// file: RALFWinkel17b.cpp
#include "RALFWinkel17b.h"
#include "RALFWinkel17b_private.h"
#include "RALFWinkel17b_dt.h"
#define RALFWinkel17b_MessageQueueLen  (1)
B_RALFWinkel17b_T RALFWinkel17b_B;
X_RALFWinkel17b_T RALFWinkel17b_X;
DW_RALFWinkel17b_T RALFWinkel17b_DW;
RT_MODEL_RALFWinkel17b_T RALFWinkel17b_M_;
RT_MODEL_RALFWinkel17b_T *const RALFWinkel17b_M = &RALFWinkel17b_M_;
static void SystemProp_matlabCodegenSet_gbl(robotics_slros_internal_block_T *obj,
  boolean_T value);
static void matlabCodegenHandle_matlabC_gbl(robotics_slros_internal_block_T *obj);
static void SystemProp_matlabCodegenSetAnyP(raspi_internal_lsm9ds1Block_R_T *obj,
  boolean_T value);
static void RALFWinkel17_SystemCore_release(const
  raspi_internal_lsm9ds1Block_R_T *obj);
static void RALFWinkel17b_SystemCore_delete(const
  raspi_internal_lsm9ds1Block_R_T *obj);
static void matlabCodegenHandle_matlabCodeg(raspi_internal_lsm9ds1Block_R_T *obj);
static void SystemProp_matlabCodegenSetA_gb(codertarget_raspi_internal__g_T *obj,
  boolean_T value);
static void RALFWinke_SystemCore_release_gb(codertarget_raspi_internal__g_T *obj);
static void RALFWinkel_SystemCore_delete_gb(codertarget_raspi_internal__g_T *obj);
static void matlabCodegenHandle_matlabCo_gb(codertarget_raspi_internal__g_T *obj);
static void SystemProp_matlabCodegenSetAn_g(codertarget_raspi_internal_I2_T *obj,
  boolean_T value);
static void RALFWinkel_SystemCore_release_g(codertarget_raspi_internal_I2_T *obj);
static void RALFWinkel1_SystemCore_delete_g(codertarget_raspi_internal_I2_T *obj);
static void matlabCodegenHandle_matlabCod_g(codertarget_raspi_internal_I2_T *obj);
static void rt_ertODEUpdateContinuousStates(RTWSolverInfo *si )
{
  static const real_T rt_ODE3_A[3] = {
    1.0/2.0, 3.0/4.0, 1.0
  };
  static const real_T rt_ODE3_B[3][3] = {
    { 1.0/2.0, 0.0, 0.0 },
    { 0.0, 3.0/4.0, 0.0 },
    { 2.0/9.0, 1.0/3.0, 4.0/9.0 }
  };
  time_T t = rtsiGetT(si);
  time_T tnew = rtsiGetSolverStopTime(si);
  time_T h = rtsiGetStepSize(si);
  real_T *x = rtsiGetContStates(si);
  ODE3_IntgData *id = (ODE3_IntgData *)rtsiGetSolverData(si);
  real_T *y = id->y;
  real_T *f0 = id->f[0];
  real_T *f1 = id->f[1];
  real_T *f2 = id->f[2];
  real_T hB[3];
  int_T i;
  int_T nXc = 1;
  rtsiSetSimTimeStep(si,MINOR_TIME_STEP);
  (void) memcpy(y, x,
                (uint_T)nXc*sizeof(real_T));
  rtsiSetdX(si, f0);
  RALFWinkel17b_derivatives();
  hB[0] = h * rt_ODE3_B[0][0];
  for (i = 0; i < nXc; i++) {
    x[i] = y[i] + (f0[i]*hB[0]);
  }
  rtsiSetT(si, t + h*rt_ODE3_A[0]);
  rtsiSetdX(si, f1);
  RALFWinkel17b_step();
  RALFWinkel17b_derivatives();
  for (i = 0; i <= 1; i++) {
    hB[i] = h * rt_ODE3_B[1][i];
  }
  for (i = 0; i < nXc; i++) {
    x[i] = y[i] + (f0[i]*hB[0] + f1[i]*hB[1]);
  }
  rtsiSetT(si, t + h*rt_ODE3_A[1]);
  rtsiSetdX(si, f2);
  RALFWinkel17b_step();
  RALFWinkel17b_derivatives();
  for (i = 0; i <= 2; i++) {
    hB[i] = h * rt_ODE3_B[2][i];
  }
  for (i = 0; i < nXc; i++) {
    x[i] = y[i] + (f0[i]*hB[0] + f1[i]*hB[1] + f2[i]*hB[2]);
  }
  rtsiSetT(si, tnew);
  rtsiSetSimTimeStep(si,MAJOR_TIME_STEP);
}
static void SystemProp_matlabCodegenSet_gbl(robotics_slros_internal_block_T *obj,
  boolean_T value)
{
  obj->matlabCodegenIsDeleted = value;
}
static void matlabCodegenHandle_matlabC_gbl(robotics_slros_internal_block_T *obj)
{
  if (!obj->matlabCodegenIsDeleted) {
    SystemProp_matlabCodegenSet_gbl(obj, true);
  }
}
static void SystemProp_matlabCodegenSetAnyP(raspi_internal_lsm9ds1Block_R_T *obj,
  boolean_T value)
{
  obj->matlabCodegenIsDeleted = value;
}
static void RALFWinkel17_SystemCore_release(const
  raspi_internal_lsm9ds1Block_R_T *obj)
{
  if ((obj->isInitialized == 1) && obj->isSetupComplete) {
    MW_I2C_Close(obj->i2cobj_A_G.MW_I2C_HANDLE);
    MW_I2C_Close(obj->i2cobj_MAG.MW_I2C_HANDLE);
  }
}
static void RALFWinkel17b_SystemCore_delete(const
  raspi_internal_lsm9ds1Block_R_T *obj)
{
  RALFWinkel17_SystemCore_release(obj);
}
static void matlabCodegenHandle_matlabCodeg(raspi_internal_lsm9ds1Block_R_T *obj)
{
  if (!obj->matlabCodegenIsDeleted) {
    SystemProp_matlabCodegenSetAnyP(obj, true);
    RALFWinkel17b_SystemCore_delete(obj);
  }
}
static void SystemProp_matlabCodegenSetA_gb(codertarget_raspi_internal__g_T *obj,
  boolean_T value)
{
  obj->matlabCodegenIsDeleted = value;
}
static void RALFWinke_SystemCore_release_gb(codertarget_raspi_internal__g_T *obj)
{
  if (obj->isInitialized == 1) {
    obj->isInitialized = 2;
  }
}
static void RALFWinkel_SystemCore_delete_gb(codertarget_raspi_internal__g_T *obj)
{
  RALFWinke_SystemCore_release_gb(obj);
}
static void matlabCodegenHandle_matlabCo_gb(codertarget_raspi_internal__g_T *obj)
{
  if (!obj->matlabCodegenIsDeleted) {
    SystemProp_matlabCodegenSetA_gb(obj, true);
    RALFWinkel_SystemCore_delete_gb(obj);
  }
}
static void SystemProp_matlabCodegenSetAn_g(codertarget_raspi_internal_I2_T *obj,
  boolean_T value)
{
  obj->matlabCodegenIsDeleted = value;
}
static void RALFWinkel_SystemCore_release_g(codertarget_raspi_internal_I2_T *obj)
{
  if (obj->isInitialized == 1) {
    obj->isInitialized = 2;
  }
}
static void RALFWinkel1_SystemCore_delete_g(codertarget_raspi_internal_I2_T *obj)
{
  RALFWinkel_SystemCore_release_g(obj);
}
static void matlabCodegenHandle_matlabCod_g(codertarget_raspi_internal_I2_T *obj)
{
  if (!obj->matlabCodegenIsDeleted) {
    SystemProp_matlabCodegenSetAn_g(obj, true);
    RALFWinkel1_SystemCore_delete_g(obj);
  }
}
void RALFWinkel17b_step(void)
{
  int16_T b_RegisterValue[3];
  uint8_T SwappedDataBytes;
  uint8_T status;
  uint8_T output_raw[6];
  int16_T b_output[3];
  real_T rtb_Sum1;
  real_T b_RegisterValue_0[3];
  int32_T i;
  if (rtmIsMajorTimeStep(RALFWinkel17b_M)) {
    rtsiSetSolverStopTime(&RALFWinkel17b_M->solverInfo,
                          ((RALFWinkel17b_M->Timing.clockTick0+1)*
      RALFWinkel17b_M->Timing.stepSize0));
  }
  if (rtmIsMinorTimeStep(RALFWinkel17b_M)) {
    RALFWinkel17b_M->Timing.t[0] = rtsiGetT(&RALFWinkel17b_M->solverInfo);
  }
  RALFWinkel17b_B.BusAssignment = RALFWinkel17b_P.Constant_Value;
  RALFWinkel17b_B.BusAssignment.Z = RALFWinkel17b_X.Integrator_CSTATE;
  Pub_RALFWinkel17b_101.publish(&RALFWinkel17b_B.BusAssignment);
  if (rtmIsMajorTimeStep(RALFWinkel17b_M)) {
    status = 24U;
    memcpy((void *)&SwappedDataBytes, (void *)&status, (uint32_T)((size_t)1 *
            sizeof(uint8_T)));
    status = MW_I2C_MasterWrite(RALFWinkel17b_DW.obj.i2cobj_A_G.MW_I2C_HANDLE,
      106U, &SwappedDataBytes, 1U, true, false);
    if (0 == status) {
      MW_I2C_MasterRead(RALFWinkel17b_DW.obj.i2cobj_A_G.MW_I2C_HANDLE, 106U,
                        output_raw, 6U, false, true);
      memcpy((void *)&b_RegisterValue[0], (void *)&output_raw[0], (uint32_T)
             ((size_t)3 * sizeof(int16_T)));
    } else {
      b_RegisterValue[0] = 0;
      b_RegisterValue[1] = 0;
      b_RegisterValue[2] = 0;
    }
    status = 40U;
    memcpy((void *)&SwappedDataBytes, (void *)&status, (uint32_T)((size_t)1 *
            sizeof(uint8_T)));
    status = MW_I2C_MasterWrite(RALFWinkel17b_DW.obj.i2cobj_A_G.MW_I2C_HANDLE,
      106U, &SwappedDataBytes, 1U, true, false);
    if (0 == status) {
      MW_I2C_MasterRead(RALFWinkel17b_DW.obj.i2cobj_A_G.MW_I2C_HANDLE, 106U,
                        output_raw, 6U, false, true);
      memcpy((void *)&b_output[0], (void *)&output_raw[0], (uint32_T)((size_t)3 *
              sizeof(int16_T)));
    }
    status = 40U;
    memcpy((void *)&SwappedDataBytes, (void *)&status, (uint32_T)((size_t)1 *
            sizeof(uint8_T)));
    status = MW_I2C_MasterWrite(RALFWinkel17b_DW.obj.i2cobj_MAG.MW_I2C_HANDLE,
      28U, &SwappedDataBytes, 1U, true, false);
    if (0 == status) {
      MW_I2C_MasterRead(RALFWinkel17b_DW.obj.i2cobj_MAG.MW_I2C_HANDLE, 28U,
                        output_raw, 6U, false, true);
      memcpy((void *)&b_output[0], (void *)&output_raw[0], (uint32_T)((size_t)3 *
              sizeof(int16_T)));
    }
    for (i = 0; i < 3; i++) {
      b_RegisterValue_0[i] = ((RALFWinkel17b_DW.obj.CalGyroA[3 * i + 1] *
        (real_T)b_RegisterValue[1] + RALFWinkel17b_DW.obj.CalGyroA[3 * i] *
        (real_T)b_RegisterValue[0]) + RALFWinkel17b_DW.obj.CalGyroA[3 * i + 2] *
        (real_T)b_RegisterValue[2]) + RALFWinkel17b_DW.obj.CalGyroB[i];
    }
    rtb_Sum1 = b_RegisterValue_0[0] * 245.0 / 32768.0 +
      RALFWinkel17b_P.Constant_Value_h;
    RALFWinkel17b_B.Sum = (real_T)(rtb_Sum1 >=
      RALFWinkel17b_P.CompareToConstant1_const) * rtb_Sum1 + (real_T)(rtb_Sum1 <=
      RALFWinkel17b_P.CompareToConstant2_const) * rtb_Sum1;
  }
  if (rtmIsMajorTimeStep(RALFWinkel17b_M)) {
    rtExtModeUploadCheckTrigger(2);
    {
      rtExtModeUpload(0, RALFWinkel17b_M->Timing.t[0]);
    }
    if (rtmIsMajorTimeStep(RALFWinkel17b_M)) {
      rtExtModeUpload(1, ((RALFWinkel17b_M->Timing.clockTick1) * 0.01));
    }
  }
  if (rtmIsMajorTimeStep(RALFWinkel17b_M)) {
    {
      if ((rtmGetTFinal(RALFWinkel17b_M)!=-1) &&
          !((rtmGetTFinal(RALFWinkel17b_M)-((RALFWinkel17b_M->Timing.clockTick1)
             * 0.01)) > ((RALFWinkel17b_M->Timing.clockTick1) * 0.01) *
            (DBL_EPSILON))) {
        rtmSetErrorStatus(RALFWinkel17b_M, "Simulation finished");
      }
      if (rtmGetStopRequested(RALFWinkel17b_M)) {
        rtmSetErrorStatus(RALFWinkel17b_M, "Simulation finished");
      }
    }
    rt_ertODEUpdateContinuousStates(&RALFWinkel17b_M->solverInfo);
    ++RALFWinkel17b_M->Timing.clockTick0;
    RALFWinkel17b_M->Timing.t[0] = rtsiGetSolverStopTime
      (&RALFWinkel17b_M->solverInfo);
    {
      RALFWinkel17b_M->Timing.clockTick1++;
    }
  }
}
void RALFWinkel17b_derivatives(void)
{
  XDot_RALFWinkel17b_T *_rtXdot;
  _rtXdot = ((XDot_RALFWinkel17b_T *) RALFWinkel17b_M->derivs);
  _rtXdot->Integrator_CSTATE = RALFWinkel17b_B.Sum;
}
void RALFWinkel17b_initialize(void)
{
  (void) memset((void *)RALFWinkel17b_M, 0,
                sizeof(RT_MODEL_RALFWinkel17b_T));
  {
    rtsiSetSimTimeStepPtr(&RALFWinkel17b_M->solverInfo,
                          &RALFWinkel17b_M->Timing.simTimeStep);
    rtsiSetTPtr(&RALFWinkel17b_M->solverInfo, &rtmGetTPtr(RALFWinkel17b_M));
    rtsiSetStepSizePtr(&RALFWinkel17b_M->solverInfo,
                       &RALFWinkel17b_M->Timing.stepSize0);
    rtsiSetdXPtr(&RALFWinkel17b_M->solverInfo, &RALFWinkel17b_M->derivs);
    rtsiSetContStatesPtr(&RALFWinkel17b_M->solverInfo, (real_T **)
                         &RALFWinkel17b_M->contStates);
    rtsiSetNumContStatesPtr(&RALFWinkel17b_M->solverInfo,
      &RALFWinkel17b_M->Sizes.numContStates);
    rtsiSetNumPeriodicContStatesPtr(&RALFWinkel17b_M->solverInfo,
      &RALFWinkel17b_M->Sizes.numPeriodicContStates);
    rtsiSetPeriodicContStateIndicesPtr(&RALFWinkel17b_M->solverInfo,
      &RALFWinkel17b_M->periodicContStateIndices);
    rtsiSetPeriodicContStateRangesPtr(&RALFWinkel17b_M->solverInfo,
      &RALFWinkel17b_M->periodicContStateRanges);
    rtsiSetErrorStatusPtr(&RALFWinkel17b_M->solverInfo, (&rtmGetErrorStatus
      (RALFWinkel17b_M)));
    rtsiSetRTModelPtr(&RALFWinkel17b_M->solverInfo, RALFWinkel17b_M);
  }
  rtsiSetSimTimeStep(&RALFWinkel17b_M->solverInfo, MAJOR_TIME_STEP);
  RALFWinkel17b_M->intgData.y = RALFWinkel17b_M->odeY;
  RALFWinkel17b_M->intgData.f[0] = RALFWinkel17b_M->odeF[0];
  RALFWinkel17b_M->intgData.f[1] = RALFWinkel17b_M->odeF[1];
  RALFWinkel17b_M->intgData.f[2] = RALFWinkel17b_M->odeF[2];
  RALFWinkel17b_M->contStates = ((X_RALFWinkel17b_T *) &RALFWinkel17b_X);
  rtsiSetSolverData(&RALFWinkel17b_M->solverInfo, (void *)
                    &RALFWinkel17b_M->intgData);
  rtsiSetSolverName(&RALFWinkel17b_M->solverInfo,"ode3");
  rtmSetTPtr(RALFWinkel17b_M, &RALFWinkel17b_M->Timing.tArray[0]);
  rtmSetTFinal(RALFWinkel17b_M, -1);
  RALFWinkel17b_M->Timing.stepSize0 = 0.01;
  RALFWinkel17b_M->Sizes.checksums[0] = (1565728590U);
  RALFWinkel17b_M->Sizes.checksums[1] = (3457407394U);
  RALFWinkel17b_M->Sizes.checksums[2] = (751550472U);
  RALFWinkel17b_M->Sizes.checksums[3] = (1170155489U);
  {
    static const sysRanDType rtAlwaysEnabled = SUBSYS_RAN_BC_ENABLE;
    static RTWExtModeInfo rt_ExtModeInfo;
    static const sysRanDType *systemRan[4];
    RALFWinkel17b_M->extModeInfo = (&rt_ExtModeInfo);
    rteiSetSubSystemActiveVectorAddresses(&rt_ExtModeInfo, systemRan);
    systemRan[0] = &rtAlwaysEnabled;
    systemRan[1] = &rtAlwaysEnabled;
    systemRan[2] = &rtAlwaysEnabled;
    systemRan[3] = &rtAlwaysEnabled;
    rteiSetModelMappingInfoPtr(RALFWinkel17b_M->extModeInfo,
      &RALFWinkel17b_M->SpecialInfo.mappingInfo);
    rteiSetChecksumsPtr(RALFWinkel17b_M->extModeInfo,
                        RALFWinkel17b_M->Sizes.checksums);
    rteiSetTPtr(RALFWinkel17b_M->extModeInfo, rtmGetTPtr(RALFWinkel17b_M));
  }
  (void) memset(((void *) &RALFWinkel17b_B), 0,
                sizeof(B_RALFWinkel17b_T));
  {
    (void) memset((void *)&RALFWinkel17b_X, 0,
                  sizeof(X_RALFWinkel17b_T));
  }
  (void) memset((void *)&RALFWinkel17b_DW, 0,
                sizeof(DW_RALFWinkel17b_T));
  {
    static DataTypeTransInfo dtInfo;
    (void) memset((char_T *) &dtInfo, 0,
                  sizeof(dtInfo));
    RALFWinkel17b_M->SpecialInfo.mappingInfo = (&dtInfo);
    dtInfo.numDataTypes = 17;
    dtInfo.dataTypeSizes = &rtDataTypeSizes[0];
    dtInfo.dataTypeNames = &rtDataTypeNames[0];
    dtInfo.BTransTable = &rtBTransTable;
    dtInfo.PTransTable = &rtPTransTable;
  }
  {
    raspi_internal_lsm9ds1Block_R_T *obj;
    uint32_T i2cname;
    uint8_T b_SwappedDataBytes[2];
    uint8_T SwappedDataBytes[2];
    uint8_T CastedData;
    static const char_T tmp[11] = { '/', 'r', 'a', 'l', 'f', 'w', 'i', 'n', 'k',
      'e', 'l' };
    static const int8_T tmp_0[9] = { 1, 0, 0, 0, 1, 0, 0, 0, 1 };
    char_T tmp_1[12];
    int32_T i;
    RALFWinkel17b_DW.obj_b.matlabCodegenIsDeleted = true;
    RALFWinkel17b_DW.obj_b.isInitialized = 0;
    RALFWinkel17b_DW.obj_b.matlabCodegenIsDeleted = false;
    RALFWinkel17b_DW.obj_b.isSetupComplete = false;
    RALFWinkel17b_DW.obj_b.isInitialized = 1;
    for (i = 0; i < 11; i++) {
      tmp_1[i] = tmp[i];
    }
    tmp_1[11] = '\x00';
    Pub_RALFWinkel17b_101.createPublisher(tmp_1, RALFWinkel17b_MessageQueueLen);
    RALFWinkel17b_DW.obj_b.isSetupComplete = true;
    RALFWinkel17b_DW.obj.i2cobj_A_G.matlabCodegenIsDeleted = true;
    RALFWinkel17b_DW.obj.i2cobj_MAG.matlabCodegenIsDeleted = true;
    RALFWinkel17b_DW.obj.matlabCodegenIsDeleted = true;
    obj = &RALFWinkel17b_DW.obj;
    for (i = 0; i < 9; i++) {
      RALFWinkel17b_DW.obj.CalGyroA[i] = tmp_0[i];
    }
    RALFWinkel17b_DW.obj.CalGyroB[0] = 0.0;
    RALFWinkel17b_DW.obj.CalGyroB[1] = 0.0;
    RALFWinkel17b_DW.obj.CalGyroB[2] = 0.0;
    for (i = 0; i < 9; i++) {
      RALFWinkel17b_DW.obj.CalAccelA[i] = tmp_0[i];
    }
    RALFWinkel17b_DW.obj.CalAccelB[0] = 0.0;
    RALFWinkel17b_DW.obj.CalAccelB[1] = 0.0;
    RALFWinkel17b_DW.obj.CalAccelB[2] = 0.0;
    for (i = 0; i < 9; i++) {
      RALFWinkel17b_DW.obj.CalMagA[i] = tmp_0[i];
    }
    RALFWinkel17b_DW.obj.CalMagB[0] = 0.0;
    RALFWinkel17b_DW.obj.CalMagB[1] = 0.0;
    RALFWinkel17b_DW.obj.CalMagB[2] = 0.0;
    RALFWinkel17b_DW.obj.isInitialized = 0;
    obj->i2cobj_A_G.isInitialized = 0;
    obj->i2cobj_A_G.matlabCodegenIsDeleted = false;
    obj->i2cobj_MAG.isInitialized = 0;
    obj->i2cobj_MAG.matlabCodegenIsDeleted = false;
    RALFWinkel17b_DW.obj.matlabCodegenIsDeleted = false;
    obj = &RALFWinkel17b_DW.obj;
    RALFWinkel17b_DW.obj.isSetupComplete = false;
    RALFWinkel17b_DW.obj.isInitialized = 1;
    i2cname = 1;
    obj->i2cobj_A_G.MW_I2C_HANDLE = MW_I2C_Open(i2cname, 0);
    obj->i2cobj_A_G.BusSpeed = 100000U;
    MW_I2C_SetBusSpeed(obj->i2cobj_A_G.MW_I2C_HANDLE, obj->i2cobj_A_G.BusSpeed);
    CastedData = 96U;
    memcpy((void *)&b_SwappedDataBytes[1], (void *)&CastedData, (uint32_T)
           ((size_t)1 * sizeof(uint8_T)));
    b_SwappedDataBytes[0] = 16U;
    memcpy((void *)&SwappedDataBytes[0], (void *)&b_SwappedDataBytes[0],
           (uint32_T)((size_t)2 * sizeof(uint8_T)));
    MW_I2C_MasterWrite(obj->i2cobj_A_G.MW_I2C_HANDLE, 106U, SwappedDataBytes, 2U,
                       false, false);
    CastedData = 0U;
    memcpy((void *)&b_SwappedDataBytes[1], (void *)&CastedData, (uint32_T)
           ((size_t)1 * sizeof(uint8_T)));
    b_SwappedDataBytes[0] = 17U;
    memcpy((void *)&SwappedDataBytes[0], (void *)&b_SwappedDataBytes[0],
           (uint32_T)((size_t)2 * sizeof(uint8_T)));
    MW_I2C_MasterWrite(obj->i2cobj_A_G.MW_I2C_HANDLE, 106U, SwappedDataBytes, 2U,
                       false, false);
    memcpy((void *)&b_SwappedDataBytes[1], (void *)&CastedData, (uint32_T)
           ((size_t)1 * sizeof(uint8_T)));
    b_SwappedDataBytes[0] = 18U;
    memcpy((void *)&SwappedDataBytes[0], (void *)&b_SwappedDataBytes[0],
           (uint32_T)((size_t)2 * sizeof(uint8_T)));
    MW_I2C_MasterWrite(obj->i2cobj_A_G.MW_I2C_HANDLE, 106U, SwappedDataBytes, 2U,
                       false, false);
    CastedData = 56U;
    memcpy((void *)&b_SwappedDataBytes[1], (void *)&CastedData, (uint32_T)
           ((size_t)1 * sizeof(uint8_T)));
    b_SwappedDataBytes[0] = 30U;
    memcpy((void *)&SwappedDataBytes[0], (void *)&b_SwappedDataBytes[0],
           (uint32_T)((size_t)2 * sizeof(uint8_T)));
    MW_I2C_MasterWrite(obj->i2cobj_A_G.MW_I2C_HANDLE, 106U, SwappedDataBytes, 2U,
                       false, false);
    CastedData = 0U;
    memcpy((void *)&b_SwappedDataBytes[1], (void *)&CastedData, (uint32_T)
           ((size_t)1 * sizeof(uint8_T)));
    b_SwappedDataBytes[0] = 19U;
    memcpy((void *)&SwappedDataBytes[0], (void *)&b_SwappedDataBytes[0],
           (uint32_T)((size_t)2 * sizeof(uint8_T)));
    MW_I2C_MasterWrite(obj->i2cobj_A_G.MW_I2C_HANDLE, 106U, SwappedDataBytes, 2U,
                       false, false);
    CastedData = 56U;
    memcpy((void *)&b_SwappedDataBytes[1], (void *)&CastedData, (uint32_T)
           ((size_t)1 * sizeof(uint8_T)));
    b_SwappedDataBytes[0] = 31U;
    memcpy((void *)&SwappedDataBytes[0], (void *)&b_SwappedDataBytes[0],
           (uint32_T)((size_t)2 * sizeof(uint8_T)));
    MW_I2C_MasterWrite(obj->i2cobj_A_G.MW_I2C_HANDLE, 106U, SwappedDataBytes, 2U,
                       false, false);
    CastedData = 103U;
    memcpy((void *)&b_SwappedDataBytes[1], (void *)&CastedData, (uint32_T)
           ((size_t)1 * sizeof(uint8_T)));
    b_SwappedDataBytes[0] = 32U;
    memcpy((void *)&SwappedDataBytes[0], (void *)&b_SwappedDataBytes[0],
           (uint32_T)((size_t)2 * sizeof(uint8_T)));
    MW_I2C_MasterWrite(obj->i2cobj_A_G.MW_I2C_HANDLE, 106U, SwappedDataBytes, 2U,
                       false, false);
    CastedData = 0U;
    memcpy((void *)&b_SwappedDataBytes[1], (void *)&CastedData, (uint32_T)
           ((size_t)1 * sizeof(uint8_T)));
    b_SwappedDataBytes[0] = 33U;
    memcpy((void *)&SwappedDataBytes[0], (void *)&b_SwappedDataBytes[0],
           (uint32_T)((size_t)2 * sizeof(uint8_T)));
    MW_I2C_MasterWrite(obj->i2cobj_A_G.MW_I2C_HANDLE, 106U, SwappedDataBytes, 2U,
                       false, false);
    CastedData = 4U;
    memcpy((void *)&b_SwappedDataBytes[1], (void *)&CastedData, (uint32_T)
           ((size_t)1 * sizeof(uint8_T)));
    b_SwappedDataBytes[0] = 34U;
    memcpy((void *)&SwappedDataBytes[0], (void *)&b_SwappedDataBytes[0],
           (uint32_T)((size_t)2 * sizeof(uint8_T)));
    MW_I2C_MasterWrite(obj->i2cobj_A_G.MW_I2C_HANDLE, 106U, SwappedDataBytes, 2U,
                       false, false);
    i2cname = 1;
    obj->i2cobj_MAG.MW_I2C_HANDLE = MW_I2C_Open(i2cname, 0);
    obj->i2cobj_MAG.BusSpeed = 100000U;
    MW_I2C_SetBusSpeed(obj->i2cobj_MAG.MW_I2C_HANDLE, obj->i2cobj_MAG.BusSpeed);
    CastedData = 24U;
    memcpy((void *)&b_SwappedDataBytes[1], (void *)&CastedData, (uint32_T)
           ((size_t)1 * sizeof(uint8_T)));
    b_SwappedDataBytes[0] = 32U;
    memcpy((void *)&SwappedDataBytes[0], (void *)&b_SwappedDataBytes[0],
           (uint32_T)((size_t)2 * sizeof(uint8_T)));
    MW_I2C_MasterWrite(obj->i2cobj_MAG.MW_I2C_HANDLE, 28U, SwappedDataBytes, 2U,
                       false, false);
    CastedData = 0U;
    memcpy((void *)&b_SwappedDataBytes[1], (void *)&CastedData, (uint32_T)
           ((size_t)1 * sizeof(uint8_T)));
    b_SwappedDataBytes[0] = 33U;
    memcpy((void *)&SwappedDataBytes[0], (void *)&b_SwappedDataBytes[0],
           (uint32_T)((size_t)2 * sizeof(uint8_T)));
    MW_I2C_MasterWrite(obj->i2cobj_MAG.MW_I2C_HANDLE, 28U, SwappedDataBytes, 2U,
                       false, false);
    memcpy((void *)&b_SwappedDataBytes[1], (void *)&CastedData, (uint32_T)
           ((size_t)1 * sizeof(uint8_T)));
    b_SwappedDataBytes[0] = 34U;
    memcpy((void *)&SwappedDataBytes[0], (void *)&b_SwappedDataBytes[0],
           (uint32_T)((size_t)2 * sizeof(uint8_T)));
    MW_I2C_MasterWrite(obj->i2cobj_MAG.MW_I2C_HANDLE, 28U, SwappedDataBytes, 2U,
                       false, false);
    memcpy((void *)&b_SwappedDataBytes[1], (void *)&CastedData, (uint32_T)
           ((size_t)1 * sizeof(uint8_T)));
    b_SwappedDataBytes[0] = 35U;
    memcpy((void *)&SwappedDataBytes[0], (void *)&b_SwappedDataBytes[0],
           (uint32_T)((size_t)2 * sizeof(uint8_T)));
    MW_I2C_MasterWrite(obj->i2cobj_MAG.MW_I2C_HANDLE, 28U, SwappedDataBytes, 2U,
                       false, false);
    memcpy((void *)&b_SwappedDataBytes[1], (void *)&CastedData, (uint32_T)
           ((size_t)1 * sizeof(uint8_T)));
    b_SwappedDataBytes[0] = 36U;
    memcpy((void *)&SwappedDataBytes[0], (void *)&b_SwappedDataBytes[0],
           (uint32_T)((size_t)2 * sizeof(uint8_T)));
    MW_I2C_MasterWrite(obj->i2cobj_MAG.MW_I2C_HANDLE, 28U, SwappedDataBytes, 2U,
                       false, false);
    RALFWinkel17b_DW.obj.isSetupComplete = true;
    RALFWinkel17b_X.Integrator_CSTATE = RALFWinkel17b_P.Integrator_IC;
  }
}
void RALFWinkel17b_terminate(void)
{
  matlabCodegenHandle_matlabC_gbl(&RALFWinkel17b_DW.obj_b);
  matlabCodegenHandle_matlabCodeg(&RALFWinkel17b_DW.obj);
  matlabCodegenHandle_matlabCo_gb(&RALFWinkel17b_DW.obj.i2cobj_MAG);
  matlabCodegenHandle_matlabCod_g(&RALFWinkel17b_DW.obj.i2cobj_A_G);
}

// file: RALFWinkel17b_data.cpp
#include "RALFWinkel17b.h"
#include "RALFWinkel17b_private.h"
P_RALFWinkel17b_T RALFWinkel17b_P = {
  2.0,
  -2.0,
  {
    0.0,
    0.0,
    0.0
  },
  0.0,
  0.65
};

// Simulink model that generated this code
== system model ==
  Publish#1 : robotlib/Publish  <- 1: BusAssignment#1
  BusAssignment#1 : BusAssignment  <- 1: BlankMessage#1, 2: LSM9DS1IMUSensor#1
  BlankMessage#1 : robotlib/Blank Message
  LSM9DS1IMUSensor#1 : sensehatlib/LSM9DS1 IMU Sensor
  Publish#2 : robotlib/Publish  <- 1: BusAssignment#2
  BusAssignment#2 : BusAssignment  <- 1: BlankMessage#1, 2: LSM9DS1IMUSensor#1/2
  Publish#3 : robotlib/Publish  <- 1: BusAssignment
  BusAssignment : BusAssignment  <- 1: BlankMessage#1, 2: DataTypeConversion#1
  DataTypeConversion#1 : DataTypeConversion  <- 1: Integrator
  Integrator : Integrator  <- 1: Sum
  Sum : Sum  Inputs=++  <- 1: Product#1, 2: Product#2
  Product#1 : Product  <- 1: Sum1, 2: CompareToConstant1
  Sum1 : Sum  Inputs=++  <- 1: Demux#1, 2: Constant
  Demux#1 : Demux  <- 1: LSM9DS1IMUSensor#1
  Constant : Constant  Value=0.65
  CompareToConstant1 : simulink/Logic and Bit Operations/Compare To Constant  relop=>=  const=2  <- 1: Sum1
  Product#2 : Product  <- 1: CompareToConstant2, 2: Sum1
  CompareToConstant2 : simulink/Logic and Bit Operations/Compare To Constant  relop=<=  const=-2  <- 1: Sum1
